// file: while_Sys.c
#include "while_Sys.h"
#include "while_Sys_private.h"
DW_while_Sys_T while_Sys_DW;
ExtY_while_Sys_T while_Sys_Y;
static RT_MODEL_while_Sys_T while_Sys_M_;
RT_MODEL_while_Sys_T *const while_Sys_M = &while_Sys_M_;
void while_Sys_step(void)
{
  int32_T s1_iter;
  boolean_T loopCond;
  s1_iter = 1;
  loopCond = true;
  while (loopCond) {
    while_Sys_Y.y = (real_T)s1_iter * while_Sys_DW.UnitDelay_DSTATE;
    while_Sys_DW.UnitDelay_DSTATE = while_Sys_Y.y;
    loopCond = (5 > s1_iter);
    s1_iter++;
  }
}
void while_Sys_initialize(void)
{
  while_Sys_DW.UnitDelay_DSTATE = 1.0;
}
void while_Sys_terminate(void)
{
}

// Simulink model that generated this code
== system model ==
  Outport#1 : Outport  <- 1: Subsystem#1
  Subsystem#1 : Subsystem  <- 1: Constant#1, 2: Constant#2
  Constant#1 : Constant
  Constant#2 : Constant  Value=5
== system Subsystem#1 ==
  Inport#1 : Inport
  Inport#2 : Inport
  WhileIterator#1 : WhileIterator  MaxIters=-1  <- 1: RelationalOperator#1, 2: Inport#1
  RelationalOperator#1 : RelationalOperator  Operator=>  <- 1: Inport#2, 2: WhileIterator#1
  Outport#2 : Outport  <- 1: MATLABFunction#1
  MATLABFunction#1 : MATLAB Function  <- 1: WhileIterator#1, 2: UnitDelay
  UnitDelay : UnitDelay  InitialCondition=1  <- 1: MATLABFunction#1

